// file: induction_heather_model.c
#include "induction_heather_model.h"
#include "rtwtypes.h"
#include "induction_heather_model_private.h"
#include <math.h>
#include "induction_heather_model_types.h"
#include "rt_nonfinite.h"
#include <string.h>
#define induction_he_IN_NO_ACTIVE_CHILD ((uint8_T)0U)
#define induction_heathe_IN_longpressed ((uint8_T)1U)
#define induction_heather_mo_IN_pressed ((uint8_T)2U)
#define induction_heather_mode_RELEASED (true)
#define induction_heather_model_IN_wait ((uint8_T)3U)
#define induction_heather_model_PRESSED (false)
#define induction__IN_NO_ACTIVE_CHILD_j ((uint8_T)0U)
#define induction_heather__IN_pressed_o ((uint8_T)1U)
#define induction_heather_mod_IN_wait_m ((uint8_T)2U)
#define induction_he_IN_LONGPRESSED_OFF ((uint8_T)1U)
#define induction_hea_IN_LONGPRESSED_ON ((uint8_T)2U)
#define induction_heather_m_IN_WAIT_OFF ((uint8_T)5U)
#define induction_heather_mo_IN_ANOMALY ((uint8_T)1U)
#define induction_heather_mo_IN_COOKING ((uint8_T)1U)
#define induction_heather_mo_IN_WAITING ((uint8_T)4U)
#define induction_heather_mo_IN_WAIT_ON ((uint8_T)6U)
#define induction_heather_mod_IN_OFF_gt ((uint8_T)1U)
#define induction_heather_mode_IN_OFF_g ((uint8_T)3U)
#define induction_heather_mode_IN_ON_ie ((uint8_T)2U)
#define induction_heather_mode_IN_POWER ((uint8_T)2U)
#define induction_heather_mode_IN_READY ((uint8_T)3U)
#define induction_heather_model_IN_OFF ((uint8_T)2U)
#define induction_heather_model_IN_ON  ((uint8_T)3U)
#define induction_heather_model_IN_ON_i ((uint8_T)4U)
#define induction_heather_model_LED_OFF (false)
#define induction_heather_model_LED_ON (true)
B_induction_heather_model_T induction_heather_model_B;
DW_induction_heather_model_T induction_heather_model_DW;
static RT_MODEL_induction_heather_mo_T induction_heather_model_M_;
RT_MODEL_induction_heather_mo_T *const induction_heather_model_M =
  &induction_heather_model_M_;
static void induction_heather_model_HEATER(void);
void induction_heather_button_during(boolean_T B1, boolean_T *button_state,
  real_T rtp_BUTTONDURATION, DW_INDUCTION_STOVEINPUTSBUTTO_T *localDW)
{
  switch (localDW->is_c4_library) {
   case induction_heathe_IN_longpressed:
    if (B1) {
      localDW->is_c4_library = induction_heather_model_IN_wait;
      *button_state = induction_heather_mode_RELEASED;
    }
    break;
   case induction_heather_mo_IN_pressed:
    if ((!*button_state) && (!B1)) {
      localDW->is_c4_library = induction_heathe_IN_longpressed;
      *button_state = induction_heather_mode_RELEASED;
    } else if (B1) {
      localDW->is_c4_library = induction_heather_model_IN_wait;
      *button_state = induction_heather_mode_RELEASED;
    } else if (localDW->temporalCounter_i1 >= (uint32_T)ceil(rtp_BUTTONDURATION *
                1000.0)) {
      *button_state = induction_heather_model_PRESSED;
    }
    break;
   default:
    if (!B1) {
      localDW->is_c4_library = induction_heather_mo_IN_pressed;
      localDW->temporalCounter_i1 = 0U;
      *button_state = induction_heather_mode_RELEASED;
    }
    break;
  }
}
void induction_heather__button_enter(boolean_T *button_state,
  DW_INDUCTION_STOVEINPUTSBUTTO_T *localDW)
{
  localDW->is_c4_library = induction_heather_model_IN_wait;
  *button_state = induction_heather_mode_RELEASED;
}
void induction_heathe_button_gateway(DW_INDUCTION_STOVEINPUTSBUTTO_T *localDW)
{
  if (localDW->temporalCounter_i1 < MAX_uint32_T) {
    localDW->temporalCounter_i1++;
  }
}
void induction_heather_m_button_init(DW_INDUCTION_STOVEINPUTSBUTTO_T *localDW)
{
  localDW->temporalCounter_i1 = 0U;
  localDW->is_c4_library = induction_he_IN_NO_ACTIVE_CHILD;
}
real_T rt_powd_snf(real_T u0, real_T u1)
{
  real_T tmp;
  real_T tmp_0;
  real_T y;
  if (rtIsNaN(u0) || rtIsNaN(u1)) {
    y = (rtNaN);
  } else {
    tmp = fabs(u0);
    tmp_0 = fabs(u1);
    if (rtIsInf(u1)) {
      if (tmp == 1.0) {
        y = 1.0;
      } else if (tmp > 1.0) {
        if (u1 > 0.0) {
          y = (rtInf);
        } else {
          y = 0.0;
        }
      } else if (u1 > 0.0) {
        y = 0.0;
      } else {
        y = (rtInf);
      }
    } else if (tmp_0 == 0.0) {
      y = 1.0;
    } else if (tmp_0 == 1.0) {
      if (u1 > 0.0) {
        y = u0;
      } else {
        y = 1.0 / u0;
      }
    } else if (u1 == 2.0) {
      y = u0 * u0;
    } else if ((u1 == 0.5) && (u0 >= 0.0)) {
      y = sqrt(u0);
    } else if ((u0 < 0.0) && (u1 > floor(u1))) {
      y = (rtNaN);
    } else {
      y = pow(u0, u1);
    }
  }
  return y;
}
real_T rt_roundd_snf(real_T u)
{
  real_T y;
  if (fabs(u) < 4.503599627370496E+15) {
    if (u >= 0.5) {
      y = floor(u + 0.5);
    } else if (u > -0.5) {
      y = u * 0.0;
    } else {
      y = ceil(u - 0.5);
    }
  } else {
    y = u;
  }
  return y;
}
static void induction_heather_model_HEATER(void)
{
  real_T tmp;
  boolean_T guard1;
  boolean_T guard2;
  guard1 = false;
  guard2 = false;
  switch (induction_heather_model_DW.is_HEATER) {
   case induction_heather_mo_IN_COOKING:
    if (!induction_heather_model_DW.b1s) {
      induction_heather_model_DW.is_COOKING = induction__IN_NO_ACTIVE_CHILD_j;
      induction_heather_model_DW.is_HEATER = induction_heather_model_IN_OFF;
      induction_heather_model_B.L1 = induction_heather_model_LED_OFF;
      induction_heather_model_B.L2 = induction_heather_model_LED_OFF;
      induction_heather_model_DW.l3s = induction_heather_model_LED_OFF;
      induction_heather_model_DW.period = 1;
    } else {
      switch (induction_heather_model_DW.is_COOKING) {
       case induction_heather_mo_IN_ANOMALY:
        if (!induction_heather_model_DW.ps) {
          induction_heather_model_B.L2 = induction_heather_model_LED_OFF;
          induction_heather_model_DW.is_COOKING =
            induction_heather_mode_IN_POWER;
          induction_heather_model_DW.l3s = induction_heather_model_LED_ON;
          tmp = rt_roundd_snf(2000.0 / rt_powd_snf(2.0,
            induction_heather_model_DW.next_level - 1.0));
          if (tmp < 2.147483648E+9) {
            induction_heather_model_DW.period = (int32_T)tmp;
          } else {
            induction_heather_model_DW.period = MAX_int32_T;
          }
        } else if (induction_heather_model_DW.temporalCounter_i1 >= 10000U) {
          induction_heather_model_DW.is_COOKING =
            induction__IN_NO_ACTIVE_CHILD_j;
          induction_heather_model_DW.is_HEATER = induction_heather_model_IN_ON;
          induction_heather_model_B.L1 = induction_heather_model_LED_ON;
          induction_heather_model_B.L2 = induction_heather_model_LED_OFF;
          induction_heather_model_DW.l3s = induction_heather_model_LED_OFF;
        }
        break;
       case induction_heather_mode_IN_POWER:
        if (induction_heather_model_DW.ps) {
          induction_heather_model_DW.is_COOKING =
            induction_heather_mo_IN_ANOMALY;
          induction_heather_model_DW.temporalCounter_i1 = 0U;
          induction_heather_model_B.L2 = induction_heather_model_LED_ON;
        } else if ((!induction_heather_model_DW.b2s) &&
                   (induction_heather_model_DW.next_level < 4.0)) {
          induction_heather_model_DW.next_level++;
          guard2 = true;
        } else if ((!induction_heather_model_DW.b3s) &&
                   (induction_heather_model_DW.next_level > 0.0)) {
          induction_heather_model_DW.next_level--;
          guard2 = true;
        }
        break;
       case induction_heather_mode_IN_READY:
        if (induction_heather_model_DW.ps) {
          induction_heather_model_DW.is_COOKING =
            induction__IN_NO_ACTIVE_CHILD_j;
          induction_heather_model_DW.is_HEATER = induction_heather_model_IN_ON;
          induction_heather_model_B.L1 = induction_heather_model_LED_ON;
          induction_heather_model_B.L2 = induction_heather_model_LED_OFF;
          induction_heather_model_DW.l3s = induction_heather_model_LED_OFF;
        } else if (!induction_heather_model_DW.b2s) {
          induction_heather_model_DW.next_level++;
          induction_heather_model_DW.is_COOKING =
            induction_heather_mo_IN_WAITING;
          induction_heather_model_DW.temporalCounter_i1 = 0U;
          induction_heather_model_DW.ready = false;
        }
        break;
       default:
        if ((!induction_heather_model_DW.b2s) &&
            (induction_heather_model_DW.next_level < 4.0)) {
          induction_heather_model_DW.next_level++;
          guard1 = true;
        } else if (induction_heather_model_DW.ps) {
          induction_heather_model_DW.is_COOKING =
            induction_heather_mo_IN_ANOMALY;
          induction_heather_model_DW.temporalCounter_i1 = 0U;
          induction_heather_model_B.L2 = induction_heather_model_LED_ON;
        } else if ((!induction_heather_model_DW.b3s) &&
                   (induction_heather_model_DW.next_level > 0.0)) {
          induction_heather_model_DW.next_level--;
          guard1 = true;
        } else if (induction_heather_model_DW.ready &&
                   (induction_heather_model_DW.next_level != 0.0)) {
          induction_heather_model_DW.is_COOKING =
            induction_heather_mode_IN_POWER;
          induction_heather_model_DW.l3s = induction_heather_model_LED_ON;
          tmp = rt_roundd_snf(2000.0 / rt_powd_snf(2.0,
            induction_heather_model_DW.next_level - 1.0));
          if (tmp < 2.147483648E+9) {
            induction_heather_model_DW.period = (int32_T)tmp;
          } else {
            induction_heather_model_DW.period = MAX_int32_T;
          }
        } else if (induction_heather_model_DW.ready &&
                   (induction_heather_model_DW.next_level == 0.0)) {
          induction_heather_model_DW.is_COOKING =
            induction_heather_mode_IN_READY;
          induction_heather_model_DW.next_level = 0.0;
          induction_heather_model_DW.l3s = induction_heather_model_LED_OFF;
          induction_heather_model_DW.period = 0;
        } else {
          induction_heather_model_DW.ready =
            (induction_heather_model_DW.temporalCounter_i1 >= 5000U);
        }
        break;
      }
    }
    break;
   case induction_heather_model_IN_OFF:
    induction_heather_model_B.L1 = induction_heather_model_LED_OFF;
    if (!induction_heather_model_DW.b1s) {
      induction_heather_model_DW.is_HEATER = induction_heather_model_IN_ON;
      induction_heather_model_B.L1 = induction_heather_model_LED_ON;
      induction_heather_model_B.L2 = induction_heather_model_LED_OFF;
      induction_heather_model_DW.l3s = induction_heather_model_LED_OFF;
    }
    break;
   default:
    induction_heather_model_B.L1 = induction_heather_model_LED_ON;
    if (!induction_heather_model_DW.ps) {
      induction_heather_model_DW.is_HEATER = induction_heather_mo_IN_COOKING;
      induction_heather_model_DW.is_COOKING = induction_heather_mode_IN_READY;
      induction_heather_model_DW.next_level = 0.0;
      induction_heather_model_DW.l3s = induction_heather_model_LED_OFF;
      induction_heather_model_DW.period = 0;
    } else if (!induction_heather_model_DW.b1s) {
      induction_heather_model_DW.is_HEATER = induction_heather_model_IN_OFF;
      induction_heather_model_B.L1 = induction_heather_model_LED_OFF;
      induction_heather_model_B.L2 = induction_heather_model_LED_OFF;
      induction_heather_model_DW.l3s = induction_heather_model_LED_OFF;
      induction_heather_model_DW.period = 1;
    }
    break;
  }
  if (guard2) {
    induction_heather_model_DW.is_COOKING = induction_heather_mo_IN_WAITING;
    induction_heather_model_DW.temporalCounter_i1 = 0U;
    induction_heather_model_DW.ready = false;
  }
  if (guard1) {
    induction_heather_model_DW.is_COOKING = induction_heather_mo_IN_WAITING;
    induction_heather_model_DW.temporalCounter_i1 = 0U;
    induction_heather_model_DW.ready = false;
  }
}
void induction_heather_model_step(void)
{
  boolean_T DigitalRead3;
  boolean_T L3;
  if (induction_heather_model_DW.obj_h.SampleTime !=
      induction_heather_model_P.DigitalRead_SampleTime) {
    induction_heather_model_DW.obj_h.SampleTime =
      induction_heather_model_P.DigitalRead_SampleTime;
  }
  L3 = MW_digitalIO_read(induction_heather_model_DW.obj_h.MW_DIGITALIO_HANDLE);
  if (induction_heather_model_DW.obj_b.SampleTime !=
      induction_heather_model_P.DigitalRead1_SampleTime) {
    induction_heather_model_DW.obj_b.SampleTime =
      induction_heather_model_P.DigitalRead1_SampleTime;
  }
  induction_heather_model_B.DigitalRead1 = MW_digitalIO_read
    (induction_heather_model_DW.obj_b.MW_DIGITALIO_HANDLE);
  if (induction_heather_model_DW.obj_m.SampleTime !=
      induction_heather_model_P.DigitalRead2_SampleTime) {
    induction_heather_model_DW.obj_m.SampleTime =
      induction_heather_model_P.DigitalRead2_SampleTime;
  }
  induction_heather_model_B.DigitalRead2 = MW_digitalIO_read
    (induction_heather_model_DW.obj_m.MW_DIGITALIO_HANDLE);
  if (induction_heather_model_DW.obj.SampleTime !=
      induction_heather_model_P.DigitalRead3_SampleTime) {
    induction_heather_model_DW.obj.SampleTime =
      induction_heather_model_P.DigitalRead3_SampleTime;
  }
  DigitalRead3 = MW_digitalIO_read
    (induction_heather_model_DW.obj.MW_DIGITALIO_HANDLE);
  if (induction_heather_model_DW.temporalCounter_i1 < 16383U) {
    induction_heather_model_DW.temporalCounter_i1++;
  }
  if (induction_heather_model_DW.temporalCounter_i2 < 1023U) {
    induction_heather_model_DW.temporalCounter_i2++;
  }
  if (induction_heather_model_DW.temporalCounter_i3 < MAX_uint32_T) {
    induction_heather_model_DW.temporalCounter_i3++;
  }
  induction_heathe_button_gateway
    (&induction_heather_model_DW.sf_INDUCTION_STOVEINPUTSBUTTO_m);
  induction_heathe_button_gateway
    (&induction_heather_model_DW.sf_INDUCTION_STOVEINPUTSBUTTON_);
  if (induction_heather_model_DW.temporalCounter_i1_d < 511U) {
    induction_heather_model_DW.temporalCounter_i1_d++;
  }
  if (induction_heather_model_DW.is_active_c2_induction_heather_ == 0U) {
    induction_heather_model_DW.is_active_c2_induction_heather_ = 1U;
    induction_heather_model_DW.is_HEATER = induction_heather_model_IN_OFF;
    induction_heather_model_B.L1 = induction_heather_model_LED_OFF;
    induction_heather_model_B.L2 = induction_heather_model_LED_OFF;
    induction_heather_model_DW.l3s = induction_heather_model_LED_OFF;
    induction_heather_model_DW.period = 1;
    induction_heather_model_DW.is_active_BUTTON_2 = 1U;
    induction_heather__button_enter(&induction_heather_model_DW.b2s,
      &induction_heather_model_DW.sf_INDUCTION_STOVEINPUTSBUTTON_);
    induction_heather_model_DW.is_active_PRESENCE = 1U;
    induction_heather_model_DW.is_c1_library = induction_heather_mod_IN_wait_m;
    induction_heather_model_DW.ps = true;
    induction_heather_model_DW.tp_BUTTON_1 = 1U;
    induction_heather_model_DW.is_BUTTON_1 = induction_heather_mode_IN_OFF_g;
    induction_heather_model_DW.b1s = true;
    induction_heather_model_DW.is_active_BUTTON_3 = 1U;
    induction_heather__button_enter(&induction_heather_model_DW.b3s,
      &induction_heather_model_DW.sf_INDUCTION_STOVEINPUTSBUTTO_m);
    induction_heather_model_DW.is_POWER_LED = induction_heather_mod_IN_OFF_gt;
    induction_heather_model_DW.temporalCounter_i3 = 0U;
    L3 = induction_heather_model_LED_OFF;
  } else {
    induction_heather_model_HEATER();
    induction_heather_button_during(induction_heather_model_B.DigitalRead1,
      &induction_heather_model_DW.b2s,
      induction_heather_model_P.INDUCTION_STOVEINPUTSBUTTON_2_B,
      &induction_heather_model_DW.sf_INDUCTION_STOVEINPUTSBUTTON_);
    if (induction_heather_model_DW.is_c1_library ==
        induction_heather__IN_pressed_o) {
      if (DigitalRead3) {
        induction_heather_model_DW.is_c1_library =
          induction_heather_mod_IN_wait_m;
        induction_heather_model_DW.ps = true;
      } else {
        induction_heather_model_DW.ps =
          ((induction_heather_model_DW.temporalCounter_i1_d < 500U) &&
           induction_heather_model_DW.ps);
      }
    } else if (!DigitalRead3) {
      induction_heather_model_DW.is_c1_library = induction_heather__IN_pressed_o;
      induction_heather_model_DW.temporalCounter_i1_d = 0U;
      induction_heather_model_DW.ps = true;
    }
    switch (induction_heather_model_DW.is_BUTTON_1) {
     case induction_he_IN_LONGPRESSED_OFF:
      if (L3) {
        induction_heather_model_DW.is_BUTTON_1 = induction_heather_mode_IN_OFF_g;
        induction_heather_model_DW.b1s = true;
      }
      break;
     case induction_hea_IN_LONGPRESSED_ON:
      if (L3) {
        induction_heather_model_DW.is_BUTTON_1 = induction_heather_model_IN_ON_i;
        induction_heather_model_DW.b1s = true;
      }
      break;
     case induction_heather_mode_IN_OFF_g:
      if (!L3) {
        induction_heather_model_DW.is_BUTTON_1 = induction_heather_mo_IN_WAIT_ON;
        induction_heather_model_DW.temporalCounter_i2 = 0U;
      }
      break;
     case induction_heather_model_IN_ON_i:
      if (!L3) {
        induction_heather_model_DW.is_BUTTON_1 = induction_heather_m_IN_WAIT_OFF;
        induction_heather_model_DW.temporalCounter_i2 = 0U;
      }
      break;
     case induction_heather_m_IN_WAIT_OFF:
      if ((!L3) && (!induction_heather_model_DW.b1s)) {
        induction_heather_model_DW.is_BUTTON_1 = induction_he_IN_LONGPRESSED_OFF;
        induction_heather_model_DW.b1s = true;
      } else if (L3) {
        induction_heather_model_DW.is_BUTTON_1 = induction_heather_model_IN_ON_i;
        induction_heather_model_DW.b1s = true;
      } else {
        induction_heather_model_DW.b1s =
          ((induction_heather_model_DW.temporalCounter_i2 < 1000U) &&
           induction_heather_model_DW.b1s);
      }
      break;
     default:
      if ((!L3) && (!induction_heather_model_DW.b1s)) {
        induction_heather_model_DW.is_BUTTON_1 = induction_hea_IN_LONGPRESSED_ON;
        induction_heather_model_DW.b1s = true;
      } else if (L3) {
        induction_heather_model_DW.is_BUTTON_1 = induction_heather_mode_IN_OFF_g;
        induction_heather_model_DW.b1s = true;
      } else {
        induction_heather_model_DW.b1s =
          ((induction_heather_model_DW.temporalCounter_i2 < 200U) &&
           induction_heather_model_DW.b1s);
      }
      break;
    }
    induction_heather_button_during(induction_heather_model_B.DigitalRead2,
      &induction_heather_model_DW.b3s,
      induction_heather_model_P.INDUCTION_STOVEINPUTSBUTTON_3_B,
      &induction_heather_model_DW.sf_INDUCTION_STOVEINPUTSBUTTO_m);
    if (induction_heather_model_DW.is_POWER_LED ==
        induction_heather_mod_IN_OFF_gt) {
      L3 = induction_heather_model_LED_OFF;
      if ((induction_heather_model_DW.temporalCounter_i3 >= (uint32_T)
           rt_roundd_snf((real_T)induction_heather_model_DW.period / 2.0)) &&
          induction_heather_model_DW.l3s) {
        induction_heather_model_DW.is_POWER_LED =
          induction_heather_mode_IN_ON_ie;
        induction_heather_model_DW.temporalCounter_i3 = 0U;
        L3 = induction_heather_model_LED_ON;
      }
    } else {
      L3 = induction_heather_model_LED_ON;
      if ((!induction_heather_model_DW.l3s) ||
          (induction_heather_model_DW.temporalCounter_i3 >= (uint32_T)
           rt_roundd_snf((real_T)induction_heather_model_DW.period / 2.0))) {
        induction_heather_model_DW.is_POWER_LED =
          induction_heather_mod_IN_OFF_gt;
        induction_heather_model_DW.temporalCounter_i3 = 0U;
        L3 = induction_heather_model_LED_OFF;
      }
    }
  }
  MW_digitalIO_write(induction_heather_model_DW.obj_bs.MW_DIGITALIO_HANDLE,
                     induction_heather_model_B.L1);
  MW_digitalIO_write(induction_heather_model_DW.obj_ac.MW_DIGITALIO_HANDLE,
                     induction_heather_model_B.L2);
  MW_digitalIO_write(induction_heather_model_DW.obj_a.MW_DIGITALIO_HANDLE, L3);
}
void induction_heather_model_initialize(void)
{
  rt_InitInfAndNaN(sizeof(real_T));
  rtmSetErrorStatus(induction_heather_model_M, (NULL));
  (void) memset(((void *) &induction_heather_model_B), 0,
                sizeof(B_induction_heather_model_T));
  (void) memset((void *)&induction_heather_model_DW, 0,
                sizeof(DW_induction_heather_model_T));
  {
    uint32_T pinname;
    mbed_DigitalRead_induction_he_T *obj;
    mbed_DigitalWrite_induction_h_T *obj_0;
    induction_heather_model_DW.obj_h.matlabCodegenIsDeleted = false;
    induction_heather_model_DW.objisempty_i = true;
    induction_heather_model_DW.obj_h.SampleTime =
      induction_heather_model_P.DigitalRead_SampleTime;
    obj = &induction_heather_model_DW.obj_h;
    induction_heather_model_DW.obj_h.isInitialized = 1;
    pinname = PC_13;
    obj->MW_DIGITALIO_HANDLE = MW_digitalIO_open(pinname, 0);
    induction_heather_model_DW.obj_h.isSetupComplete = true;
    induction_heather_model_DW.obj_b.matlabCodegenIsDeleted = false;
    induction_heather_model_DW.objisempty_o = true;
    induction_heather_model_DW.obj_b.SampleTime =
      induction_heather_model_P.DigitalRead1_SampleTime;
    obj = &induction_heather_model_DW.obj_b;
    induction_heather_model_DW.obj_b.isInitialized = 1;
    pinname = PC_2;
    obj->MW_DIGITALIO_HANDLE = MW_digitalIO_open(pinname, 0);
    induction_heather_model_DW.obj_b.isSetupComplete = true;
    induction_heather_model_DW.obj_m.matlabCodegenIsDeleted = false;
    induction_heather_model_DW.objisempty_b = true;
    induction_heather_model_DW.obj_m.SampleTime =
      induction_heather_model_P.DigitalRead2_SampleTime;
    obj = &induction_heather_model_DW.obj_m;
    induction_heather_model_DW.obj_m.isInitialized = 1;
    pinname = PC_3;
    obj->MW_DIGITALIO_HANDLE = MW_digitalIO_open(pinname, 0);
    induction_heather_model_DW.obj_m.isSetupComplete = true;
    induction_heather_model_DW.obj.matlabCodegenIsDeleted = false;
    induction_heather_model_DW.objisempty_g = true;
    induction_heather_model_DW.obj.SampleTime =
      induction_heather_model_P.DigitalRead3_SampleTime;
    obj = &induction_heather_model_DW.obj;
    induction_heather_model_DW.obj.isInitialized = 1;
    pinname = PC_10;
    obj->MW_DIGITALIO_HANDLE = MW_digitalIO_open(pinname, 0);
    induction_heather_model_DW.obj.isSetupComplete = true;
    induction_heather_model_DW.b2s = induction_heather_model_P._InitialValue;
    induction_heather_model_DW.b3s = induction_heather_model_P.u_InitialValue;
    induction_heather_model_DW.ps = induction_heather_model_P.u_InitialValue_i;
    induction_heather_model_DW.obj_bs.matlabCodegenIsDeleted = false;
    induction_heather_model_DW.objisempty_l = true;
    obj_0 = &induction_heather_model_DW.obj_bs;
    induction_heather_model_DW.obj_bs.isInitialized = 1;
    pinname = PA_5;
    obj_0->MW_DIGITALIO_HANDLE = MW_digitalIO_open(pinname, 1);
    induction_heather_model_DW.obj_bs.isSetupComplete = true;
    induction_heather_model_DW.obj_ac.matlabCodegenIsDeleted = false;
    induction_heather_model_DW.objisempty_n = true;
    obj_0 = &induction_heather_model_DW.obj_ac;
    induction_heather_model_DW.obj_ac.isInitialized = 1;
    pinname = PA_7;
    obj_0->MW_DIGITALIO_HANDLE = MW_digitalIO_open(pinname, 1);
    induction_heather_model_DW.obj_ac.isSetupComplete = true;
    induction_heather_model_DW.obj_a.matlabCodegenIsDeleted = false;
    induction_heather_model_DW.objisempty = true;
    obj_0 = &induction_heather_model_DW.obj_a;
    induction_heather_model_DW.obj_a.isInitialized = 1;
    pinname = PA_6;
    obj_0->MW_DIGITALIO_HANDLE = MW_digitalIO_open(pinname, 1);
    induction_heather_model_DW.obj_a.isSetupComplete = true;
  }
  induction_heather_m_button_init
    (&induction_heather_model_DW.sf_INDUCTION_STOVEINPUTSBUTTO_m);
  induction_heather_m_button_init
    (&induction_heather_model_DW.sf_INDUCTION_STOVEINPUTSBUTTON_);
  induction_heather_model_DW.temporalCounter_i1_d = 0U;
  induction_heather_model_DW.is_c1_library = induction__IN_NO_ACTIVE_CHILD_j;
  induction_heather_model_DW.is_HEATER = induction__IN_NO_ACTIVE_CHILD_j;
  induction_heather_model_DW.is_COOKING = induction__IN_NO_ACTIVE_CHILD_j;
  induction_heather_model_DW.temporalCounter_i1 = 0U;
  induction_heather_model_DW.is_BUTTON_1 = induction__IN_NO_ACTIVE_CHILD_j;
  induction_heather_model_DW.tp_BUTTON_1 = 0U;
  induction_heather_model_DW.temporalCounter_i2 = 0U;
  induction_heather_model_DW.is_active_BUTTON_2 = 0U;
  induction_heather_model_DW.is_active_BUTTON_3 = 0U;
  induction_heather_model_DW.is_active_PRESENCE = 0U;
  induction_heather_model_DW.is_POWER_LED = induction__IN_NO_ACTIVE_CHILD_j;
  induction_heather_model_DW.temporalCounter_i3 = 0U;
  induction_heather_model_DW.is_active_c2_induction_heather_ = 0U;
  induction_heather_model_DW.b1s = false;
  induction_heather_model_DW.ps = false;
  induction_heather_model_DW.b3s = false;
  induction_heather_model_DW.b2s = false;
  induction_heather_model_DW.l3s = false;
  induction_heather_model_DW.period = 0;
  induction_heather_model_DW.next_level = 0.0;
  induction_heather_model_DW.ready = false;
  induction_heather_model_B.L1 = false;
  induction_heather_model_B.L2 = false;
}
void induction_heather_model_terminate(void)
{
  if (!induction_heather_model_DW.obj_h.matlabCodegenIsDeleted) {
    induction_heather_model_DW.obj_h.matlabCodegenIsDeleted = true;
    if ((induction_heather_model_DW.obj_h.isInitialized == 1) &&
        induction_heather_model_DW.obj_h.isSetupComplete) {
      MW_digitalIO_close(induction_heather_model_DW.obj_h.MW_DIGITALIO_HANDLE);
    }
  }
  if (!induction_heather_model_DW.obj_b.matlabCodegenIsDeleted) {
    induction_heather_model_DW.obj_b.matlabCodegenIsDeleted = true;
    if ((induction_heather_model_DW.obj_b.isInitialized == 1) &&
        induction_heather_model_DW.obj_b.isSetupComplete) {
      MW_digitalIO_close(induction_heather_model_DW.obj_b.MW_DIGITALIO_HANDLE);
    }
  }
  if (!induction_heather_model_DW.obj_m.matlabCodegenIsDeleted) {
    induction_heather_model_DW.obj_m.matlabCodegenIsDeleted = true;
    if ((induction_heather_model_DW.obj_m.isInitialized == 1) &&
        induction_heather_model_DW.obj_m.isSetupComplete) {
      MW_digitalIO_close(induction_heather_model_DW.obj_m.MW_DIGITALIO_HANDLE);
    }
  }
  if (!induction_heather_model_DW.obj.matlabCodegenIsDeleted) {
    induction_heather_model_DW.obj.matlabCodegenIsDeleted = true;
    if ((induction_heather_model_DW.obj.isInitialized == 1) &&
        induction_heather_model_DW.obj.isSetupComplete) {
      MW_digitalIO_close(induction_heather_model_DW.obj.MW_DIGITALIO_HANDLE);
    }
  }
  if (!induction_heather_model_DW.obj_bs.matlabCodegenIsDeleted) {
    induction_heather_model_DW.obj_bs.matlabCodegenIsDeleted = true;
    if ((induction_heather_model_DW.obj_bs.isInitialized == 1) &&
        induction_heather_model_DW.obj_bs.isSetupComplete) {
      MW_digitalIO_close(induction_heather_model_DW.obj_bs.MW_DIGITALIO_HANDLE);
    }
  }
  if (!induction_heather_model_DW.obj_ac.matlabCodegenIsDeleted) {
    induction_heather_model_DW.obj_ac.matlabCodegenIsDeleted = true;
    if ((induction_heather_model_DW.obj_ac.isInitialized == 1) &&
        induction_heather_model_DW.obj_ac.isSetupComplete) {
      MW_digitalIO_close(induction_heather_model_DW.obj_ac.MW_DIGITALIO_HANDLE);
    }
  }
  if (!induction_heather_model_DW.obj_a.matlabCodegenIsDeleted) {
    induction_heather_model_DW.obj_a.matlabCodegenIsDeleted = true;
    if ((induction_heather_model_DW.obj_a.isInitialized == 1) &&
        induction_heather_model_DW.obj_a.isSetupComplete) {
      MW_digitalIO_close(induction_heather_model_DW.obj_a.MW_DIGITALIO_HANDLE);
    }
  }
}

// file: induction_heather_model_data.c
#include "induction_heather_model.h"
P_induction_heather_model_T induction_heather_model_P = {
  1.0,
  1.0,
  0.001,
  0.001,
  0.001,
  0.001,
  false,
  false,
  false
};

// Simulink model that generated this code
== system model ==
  DigitalWrite : mbedblockslib/Digital Write  <- 1: Stateflowchart#1
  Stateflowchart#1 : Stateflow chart  <- 1: DigitalRead, 2: DigitalRead1, 3: DigitalRead2, 4: DigitalRead3
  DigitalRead : mbedblockslib/Digital Read
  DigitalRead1 : mbedblockslib/Digital Read
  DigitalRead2 : mbedblockslib/Digital Read
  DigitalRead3 : mbedblockslib/Digital Read
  DigitalWrite#1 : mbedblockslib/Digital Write  <- 1: Stateflowchart#1/2
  DigitalWrite#2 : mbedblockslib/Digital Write  <- 1: Stateflowchart#1/3
== stateflow chart Stateflowchart#1 ==
  state INDUCTION_STOVE
    state HEATER [parallel]
      settings: executionOrder=1
      state OFF
        en: L1 = LED_OFF;
        L2 = LED_OFF;
        l3s = LED_OFF;
        period = 1;
      state COOKING
        state WAITING
          ready = false;
          on after(5, sec):
          ready = true;
        state READY
          en: level = 0;
          next_level = 0;
          l3s = LED_OFF;
          period = 0;
        state POWER
          en: level=next_level;
          l3s = LED_ON;
          period = int32( 2000/2^(level-1));
        state ANOMALY
          en: L2 = LED_ON;
          ex: L2 = LED_OFF;
        WAITING -> WAITING [order 1] : [b2s==PRESSED && next_level < 4]{next_level=next_level+1;}
        WAITING -> WAITING [order 3] : [b3s==PRESSED && next_level > 0]{next_level=next_level-1;}
        READY -> WAITING [order 2] : [b2s==PRESSED]{next_level=next_level+1;}
        WAITING -> READY [order 5] : [ready==true && next_level == 0]
        POWER -> WAITING [order 2] : [b2s==PRESSED && next_level < 4]{next_level=next_level+1;}
        POWER -> WAITING [order 3] : [b3s==PRESSED && next_level  > 0]{next_level=next_level-1;}
        WAITING -> ANOMALY [order 2] : [ps~=PRESENCE]
        WAITING -> POWER [order 4] : [ready==true && next_level ~= 0]
        POWER -> ANOMALY [order 1] : [ps~=PRESENCE]
        ANOMALY -> POWER [order 1] : [ps==PRESENCE]
      state ON
        en: L1 = LED_ON;
        L2 = LED_OFF;
        l3s = LED_OFF;
      (default) -> INDUCTION_STOVE.HEATER.OFF
      INDUCTION_STOVE.HEATER.OFF -> INDUCTION_STOVE.HEATER.ON : [b1s==PRESSED]
      INDUCTION_STOVE.HEATER.ON -> INDUCTION_STOVE.HEATER.OFF [order 2] : [b1s==PRESSED]
      COOKING -> INDUCTION_STOVE.HEATER.OFF : [b1s==PRESSED ]
      ANOMALY -> INDUCTION_STOVE.HEATER.ON [order 2] : [after(10,sec)]
      INDUCTION_STOVE.HEATER.ON -> READY [order 1] : [ps==PRESENCE]
      READY -> INDUCTION_STOVE.HEATER.ON [order 1] : [ps~=PRESENCE ]
    state INPUTS [parallel]
      settings: executionOrder=2
      state BUTTON_3 [parallel]
        settings: executionOrder=4
      state BUTTON_1 [parallel]
        settings: executionOrder=3
        state OFF
          en: b1s = ~PRESSED;
        state WAIT_ON
          en:
          on after(200, msec):
          b1s=PRESSED;
        state LONGPRESSED_OFF
          en: b1s =~PRESSED;
        state LONGPRESSED_ON
          en:
          b1s=~PRESSED;
        state WAIT_OFF
          on after(1,sec):
          b1s=PRESSED;
        state ON
          en: b1s = ~PRESSED;
        (default) -> INDUCTION_STOVE.INPUTS.BUTTON_1.OFF
        INDUCTION_STOVE.INPUTS.BUTTON_1.OFF -> WAIT_ON : [B1==PRESSED]
        WAIT_ON -> INDUCTION_STOVE.INPUTS.BUTTON_1.OFF [order 2] : [B1 ~= PRESSED]
        LONGPRESSED_OFF -> INDUCTION_STOVE.INPUTS.BUTTON_1.OFF : [B1~= PRESSED]
        WAIT_ON -> LONGPRESSED_ON [order 1] : [B1 == PRESSED && b1s == PRESSED]
        WAIT_OFF -> LONGPRESSED_OFF [order 1] : [B1==PRESSED && b1s == PRESSED]
        LONGPRESSED_ON -> INDUCTION_STOVE.INPUTS.BUTTON_1.ON : [B1 ~= PRESSED]
        INDUCTION_STOVE.INPUTS.BUTTON_1.ON -> WAIT_OFF : [B1==PRESSED]
        WAIT_OFF -> INDUCTION_STOVE.INPUTS.BUTTON_1.ON [order 2] : [B1 ~= PRESSED]
      state BUTTON_2 [parallel]
        settings: executionOrder=1
      state PRESENCE [parallel]
        settings: executionOrder=2
    state POWER_LED [parallel]
      settings: executionOrder=3
      state OFF
        entry: L3 = LED_OFF;
      state ON
        entry: L3 = LED_ON;
      (default) -> INDUCTION_STOVE.POWER_LED.OFF
      INDUCTION_STOVE.POWER_LED.ON -> INDUCTION_STOVE.POWER_LED.OFF : [l3s == LED_OFF || (after(period/2,msec) && l3s == LED_ON)]
      INDUCTION_STOVE.POWER_LED.OFF -> INDUCTION_STOVE.POWER_LED.ON : [after(period/2,msec) && l3s == LED_ON]
  data: button_state function_output; button_state function_output; presence_state function_output; B1 input boolean size=1; B2 input boolean size=1; B3 input boolean size=1; P input boolean size=1; L1 output boolean size=1; L2 output boolean size=1; L3 output boolean size=1; LED_ON constant boolean =1; LED_OFF constant boolean =0; PRESSED constant boolean =0; b1s local boolean size=1; ps local boolean size=1; PRESENCE constant boolean =0; b3s local boolean size=1; b2s local boolean size=1; l3s local boolean size=1; period local int32 size=1; level local; next_level local; ready local boolean
